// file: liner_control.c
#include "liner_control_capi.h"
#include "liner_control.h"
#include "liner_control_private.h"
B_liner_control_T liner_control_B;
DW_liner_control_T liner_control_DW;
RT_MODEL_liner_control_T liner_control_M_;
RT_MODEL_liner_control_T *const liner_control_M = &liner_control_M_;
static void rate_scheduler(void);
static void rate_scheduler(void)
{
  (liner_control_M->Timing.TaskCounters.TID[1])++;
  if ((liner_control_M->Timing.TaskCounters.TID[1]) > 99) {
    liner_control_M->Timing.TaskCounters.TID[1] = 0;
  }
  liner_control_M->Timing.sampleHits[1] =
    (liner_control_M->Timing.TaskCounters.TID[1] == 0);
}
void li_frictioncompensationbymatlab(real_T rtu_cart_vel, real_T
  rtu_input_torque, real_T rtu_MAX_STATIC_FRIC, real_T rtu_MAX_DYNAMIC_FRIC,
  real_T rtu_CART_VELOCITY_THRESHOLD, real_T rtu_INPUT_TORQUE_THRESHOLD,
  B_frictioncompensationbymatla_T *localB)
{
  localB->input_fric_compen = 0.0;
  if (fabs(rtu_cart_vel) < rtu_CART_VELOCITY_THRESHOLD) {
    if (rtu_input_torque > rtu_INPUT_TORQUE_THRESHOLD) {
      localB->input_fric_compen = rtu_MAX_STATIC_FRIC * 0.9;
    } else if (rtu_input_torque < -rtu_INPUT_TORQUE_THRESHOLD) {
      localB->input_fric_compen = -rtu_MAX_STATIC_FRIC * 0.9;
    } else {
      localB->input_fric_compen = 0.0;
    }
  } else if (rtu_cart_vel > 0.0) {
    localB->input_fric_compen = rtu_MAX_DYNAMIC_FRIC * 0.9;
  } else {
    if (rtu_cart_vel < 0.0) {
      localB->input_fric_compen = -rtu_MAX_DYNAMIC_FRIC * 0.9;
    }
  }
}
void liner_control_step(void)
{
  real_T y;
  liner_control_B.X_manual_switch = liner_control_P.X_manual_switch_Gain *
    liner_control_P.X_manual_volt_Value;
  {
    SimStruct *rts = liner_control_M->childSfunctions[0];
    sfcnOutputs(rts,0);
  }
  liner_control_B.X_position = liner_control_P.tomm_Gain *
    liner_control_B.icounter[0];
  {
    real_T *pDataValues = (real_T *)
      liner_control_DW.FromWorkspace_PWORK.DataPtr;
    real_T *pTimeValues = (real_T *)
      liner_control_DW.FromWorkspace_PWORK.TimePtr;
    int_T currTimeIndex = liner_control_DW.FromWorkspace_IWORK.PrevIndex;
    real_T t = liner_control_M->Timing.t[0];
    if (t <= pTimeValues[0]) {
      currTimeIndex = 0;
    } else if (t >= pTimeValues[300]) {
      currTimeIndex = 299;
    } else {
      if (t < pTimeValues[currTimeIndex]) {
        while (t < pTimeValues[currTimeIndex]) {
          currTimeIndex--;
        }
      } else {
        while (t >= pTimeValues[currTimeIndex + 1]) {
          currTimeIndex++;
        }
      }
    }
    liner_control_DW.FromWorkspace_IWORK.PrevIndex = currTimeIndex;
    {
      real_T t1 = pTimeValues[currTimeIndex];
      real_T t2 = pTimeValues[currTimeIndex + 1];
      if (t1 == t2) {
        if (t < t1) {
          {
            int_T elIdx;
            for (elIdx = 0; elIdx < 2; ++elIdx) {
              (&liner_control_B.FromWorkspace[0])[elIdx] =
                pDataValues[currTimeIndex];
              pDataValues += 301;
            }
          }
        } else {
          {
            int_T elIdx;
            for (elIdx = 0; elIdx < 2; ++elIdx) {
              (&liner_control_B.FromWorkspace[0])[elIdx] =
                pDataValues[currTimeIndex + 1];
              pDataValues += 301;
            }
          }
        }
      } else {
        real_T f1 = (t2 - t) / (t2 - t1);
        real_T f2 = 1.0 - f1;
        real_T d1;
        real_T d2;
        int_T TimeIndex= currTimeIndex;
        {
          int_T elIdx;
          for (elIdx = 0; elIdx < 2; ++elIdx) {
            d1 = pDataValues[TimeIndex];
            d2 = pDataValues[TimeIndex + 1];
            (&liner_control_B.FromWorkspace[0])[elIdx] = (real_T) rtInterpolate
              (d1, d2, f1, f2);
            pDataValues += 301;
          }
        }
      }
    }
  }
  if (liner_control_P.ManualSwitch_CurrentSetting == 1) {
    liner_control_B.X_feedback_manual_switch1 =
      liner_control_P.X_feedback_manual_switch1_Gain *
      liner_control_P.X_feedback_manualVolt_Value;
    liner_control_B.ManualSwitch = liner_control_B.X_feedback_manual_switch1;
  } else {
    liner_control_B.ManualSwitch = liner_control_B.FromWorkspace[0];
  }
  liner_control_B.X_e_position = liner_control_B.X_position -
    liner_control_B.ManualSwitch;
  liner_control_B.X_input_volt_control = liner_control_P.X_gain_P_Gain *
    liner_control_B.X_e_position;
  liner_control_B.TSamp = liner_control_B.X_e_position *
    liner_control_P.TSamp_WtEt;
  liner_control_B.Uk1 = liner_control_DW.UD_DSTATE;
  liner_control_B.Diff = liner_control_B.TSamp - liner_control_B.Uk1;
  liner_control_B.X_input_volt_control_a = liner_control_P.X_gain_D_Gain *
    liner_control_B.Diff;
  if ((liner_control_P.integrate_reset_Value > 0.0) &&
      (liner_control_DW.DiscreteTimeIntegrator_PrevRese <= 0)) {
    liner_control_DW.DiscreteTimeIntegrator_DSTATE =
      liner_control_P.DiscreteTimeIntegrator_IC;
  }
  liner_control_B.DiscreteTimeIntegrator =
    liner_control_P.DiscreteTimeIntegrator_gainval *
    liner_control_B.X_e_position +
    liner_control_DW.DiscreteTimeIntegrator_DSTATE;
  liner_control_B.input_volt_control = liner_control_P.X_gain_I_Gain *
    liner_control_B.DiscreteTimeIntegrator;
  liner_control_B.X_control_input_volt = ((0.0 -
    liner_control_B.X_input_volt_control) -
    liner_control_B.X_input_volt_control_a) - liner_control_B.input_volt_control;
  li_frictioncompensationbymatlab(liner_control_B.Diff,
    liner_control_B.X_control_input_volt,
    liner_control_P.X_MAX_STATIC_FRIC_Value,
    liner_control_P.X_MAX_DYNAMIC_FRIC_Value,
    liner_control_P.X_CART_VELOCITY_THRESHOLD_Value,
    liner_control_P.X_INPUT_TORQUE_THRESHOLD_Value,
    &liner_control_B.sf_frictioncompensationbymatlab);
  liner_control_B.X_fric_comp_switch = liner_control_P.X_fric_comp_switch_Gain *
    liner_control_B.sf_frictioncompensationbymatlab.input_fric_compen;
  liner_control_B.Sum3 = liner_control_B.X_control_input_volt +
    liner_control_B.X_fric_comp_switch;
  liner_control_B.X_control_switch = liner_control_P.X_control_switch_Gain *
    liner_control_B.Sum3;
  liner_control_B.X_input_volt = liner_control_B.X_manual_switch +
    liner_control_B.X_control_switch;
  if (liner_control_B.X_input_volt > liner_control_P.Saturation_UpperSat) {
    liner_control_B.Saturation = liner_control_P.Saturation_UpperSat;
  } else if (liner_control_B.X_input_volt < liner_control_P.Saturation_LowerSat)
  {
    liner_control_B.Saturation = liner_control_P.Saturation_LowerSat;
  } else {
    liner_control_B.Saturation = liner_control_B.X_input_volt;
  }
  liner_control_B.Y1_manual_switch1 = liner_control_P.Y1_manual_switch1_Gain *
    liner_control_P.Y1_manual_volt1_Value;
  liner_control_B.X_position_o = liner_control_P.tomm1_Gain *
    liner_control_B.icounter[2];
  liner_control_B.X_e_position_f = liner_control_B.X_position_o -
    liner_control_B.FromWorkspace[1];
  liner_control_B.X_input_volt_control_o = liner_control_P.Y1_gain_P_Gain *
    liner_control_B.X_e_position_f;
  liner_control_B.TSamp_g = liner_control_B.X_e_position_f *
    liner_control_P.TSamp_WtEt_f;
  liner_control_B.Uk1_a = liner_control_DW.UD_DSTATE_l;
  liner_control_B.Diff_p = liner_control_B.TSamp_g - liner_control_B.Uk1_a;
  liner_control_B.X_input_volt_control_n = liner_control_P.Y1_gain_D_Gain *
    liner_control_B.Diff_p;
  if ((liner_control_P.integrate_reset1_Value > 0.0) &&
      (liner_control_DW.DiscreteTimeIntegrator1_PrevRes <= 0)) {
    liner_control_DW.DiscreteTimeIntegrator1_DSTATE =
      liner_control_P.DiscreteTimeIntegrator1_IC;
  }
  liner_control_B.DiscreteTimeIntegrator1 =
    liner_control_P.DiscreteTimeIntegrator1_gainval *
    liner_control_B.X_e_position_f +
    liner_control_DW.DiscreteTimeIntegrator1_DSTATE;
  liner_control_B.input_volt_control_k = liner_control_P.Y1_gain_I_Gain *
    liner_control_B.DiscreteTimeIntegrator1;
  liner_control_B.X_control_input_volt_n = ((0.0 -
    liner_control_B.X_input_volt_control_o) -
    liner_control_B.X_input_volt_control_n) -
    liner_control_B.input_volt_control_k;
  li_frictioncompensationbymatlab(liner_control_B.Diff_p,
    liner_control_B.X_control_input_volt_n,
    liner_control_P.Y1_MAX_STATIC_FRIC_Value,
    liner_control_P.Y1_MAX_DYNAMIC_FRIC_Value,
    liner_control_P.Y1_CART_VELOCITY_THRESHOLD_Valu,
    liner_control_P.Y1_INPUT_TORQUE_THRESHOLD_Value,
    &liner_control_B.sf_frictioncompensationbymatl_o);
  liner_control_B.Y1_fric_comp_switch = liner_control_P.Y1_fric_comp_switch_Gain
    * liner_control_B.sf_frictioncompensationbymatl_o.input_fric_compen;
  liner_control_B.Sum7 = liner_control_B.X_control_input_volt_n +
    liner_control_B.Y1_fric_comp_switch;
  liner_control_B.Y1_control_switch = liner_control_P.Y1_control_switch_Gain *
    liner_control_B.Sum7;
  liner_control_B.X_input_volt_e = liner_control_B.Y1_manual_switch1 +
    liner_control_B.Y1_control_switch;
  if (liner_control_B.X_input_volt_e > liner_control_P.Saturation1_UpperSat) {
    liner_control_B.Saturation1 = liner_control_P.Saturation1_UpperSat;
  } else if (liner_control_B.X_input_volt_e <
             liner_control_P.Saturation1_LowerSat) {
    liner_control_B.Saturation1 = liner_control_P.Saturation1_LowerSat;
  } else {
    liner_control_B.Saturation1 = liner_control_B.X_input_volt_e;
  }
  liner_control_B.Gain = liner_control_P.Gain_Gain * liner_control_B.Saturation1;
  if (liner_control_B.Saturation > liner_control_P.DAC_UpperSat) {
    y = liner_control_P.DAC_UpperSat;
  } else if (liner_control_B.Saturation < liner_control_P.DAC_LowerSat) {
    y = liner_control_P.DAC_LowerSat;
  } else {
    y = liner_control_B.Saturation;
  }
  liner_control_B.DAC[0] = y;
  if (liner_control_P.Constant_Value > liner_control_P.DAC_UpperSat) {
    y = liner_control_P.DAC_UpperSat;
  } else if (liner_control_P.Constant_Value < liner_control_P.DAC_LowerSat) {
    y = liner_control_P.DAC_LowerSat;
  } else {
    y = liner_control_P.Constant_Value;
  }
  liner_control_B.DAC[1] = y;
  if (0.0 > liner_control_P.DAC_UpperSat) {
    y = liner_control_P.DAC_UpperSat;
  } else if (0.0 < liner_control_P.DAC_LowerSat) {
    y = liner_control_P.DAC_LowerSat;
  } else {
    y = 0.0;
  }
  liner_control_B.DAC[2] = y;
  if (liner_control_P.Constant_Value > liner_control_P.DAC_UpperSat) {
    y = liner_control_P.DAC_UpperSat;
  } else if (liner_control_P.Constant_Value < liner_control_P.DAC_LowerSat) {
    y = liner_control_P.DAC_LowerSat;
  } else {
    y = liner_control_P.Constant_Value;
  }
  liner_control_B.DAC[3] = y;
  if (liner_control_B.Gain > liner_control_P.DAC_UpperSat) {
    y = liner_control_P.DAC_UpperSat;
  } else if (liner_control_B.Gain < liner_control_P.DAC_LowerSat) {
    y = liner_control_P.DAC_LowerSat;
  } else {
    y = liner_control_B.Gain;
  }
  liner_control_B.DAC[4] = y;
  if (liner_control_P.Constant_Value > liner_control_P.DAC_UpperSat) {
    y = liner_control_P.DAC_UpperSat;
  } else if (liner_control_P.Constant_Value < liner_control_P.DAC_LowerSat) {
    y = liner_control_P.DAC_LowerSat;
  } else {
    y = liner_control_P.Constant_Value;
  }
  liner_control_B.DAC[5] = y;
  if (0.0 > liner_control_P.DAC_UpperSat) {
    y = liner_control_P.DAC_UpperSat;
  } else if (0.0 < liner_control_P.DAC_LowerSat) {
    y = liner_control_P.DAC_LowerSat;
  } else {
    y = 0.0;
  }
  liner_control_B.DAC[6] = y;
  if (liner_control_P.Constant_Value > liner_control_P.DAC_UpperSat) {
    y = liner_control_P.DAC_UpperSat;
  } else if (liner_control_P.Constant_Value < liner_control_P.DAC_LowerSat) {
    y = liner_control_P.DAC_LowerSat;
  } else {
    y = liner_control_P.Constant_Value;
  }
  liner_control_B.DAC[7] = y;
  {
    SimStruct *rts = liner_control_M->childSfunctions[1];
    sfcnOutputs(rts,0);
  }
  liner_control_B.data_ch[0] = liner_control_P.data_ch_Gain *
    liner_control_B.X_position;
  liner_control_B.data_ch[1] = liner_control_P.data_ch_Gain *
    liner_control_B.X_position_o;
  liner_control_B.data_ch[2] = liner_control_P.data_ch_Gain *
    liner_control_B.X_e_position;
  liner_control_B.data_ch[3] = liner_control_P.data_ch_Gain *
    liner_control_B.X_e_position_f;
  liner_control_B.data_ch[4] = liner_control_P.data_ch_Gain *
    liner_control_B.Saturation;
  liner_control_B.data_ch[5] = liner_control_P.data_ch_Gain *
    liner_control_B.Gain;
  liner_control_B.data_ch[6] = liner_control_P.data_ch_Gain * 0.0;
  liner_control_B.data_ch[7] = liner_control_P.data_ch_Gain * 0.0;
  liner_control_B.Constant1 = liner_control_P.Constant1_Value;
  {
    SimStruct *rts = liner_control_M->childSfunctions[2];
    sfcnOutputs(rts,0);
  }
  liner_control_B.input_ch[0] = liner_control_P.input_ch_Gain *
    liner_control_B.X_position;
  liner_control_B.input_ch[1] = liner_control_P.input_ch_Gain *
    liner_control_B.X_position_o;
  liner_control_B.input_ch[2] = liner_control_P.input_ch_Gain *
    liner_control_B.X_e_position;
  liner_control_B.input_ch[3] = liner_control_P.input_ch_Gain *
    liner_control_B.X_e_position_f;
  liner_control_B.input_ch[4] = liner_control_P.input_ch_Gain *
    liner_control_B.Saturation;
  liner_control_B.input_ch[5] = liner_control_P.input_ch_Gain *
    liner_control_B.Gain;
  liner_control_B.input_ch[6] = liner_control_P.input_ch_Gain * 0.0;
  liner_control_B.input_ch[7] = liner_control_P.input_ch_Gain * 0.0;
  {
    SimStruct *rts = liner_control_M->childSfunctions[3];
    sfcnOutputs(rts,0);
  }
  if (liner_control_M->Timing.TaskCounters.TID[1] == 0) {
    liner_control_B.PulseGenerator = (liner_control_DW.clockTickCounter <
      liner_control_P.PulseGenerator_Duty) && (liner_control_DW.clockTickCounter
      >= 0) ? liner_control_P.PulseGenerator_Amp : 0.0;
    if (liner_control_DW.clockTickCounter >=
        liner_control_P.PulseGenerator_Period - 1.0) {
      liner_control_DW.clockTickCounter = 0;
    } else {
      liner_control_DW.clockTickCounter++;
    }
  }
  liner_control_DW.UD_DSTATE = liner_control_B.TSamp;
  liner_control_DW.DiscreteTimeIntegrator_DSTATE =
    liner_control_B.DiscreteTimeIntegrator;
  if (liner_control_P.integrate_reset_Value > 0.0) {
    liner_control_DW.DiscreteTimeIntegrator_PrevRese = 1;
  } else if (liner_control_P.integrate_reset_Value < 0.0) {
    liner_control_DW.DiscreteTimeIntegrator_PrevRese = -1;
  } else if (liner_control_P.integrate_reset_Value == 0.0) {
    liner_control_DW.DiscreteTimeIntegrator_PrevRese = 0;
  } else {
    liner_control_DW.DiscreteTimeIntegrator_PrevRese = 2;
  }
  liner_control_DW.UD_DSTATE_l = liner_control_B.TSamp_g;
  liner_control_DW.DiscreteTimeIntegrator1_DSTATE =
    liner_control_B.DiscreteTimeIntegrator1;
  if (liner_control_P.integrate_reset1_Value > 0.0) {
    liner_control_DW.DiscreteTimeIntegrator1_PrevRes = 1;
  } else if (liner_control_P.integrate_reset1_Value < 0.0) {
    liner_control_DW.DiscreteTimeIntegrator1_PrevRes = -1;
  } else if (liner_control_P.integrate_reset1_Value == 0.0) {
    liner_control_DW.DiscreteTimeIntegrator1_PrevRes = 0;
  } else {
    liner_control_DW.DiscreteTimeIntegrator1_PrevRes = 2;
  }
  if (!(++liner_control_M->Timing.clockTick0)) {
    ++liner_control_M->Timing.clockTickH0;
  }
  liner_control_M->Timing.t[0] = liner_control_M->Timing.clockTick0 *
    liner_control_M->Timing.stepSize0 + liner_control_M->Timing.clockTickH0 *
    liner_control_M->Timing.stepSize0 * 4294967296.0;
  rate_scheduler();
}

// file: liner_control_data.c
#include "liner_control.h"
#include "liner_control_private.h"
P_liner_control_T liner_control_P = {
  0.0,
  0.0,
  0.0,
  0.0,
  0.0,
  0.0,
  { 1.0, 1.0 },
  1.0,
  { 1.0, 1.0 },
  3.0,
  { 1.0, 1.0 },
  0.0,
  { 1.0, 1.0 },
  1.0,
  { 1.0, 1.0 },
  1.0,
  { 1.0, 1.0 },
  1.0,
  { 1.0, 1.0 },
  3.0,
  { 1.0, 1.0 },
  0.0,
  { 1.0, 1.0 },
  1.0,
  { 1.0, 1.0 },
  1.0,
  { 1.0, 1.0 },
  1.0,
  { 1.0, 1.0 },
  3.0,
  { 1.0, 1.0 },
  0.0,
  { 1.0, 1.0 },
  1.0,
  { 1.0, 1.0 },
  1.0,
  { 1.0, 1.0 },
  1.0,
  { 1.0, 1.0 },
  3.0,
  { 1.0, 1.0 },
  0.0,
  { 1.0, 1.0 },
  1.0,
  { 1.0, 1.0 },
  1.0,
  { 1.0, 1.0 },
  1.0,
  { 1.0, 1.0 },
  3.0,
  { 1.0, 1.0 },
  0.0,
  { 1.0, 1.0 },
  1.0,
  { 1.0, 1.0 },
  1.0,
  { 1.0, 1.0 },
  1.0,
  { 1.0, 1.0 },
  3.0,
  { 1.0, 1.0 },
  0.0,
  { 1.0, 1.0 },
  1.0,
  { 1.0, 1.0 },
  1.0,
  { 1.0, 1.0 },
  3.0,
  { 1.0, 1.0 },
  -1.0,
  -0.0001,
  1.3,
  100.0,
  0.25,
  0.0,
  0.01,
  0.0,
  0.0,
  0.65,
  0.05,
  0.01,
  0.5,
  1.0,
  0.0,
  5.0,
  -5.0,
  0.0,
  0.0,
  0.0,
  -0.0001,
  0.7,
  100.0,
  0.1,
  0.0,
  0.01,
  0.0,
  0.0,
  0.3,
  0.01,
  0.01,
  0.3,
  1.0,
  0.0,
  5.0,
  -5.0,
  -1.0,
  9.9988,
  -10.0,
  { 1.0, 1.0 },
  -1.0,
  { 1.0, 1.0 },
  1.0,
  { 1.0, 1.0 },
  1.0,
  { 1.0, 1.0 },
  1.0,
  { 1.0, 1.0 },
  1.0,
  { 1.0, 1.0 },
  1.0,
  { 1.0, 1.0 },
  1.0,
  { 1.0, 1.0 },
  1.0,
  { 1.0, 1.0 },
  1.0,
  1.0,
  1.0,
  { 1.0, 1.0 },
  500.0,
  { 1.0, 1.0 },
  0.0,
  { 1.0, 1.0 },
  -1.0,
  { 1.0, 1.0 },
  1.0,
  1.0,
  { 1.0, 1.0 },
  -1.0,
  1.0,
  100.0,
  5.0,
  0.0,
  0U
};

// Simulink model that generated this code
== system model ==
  SBOX2_GRAPH_MONITOR#1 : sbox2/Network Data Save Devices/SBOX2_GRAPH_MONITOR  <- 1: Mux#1
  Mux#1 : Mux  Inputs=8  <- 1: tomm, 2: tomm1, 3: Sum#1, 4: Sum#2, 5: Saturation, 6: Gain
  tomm : Gain  Gain=-0.0001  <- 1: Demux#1
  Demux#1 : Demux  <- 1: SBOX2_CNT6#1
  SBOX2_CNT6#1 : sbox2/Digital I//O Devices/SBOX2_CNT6
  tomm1 : Gain  Gain=-0.0001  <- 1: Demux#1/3
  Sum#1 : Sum  Inputs=+-  <- 1: tomm, 2: ManualSwitch
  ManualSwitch : ManualSwitch  <- 1: X_feedback_manual_switch1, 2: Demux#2
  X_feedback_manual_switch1 : Gain  Gain=0  <- 1: X_feedback_manualVolt
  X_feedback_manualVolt : Constant  Value=0
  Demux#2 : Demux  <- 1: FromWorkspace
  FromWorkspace : FromWorkspace
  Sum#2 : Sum  Inputs=+-  <- 1: tomm1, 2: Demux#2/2
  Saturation : Saturate  UpperLimit=5  LowerLimit=-5  <- 1: Sum#3
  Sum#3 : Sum  Inputs=++  <- 1: X_manual_switch, 2: X_control_switch
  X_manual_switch : Gain  Gain=0  <- 1: X_manual_volt
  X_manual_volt : Constant  Value=0
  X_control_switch : Gain  Gain=0  <- 1: Sum3
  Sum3 : Sum  Inputs=++  <- 1: Sum#4, 2: X_fric_comp_switch
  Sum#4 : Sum  Inputs=---  <- 1: X_gain_P, 2: X_gain_D, 3: X_gain_I
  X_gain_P : Gain  Gain=1.3  <- 1: Sum#1
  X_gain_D : Gain  Gain=0.25  <- 1: DiscreteDerivative#1
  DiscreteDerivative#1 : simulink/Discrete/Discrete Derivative  gainval=1.0  <- 1: Sum#1
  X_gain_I : Gain  Gain=0  <- 1: DiscreteTimeIntegrator
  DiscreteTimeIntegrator : DiscreteIntegrator  IntegratorMethod=Integration: Backward Euler  ExternalReset=rising  <- 1: Sum#1, 2: integrate_reset
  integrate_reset : Constant  Value=0
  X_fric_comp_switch : Gain  <- 1: frictioncompensationbymatlab
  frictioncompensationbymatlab : MATLAB Function  <- 1: DiscreteDerivative#1, 2: Sum#4, 3: X_MAX_STATIC_FRIC, 4: X_MAX_DYNAMIC_FRIC, 5: X_CART_VELOCITY_THRESHOLD, 6: X_INPUT_TORQUE_THRESHOLD
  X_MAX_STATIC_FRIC : Constant  Value=0.65
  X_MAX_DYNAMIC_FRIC : Constant  Value=0.05
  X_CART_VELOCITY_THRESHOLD : Constant  Value=0.01
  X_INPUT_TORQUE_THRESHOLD : Constant  Value=0.5
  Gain : Gain  Gain=-1  <- 1: Saturation1
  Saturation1 : Saturate  UpperLimit=5  LowerLimit=-5  <- 1: Sum#5
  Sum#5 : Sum  Inputs=++  <- 1: Y1_manual_switch1, 2: Y1_control_switch
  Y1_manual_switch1 : Gain  Gain=0  <- 1: Y1_manual_volt1
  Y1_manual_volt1 : Constant  Value=0
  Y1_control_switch : Gain  Gain=0  <- 1: Sum7
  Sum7 : Sum  Inputs=++  <- 1: Sum#6, 2: Y1_fric_comp_switch
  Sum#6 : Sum  Inputs=---  <- 1: Y1_gain_P, 2: Y1_gain_D, 3: Y1_gain_I
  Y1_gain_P : Gain  Gain=0.7  <- 1: Sum#2
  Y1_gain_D : Gain  Gain=0.1  <- 1: DiscreteDerivative#2
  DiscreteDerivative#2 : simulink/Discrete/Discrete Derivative  gainval=1.0  <- 1: Sum#2
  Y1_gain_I : Gain  Gain=0  <- 1: DiscreteTimeIntegrator1
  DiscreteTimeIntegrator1 : DiscreteIntegrator  IntegratorMethod=Integration: Backward Euler  ExternalReset=rising  <- 1: Sum#2, 2: integrate_reset1
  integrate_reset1 : Constant  Value=0
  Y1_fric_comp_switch : Gain  <- 1: MATLABFunction#1
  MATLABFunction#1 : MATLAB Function  <- 1: DiscreteDerivative#2, 2: Sum#6, 3: Y1_MAX_STATIC_FRIC, 4: Y1_MAX_DYNAMIC_FRIC, 5: Y1_CART_VELOCITY_THRESHOLD, 6: Y1_INPUT_TORQUE_THRESHOLD
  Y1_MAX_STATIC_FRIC : Constant  Value=0.3
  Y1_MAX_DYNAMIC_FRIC : Constant  Value=0.01
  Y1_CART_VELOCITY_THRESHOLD : Constant  Value=0.01
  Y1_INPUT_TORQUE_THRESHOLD : Constant  Value=0.3
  SBOX2_DAM148_NET#1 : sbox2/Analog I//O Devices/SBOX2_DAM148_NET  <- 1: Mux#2
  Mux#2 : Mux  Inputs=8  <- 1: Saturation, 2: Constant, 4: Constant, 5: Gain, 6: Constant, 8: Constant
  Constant : Constant  Value=0
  SBOX2_DATA_SAVE_NET#1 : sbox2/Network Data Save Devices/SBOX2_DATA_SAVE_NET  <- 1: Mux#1, 2: Constant1
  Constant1 : Constant
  PulseGenerator : DiscretePulseGenerator  Period=100  PulseWidth=5
== matlab function frictioncompensationbymatlab ==
function input_fric_compen = fcn(cart_vel, input_torque, MAX_STATIC_FRIC, MAX_DYNAMIC_FRIC, CART_VELOCITY_THRESHOLD, INPUT_TORQUE_THRESHOLD)

input_fric_compen = zeros(1);

if abs(cart_vel) < CART_VELOCITY_THRESHOLD
    if input_torque > INPUT_TORQUE_THRESHOLD
        input_fric_compen = MAX_STATIC_FRIC * 0.9;
    else
        if input_torque < -INPUT_TORQUE_THRESHOLD
            input_fric_compen = - MAX_STATIC_FRIC * 0.9;
        else
            input_fric_compen = 0.0;
        end
    end
else
    if cart_vel > 0.0
        input_fric_compen = MAX_DYNAMIC_FRIC * 0.9;
    elseif cart_vel < 0.0
        input_fric_compen = - MAX_DYNAMIC_FRIC * 0.9;
    end
end

end

== matlab function MATLABFunction#1 ==
function input_fric_compen = fcn(cart_vel, input_torque, MAX_STATIC_FRIC, MAX_DYNAMIC_FRIC, CART_VELOCITY_THRESHOLD, INPUT_TORQUE_THRESHOLD)

input_fric_compen = zeros(1);

if abs(cart_vel) < CART_VELOCITY_THRESHOLD
    if input_torque > INPUT_TORQUE_THRESHOLD
        input_fric_compen = MAX_STATIC_FRIC * 0.9;
    else
        if input_torque < -INPUT_TORQUE_THRESHOLD
            input_fric_compen = - MAX_STATIC_FRIC * 0.9;
        else
            input_fric_compen = 0.0;
        end
    end
else
    if cart_vel > 0.0
        input_fric_compen = MAX_DYNAMIC_FRIC * 0.9;
    elseif cart_vel < 0.0
        input_fric_compen = - MAX_DYNAMIC_FRIC * 0.9;
    end
end

end
